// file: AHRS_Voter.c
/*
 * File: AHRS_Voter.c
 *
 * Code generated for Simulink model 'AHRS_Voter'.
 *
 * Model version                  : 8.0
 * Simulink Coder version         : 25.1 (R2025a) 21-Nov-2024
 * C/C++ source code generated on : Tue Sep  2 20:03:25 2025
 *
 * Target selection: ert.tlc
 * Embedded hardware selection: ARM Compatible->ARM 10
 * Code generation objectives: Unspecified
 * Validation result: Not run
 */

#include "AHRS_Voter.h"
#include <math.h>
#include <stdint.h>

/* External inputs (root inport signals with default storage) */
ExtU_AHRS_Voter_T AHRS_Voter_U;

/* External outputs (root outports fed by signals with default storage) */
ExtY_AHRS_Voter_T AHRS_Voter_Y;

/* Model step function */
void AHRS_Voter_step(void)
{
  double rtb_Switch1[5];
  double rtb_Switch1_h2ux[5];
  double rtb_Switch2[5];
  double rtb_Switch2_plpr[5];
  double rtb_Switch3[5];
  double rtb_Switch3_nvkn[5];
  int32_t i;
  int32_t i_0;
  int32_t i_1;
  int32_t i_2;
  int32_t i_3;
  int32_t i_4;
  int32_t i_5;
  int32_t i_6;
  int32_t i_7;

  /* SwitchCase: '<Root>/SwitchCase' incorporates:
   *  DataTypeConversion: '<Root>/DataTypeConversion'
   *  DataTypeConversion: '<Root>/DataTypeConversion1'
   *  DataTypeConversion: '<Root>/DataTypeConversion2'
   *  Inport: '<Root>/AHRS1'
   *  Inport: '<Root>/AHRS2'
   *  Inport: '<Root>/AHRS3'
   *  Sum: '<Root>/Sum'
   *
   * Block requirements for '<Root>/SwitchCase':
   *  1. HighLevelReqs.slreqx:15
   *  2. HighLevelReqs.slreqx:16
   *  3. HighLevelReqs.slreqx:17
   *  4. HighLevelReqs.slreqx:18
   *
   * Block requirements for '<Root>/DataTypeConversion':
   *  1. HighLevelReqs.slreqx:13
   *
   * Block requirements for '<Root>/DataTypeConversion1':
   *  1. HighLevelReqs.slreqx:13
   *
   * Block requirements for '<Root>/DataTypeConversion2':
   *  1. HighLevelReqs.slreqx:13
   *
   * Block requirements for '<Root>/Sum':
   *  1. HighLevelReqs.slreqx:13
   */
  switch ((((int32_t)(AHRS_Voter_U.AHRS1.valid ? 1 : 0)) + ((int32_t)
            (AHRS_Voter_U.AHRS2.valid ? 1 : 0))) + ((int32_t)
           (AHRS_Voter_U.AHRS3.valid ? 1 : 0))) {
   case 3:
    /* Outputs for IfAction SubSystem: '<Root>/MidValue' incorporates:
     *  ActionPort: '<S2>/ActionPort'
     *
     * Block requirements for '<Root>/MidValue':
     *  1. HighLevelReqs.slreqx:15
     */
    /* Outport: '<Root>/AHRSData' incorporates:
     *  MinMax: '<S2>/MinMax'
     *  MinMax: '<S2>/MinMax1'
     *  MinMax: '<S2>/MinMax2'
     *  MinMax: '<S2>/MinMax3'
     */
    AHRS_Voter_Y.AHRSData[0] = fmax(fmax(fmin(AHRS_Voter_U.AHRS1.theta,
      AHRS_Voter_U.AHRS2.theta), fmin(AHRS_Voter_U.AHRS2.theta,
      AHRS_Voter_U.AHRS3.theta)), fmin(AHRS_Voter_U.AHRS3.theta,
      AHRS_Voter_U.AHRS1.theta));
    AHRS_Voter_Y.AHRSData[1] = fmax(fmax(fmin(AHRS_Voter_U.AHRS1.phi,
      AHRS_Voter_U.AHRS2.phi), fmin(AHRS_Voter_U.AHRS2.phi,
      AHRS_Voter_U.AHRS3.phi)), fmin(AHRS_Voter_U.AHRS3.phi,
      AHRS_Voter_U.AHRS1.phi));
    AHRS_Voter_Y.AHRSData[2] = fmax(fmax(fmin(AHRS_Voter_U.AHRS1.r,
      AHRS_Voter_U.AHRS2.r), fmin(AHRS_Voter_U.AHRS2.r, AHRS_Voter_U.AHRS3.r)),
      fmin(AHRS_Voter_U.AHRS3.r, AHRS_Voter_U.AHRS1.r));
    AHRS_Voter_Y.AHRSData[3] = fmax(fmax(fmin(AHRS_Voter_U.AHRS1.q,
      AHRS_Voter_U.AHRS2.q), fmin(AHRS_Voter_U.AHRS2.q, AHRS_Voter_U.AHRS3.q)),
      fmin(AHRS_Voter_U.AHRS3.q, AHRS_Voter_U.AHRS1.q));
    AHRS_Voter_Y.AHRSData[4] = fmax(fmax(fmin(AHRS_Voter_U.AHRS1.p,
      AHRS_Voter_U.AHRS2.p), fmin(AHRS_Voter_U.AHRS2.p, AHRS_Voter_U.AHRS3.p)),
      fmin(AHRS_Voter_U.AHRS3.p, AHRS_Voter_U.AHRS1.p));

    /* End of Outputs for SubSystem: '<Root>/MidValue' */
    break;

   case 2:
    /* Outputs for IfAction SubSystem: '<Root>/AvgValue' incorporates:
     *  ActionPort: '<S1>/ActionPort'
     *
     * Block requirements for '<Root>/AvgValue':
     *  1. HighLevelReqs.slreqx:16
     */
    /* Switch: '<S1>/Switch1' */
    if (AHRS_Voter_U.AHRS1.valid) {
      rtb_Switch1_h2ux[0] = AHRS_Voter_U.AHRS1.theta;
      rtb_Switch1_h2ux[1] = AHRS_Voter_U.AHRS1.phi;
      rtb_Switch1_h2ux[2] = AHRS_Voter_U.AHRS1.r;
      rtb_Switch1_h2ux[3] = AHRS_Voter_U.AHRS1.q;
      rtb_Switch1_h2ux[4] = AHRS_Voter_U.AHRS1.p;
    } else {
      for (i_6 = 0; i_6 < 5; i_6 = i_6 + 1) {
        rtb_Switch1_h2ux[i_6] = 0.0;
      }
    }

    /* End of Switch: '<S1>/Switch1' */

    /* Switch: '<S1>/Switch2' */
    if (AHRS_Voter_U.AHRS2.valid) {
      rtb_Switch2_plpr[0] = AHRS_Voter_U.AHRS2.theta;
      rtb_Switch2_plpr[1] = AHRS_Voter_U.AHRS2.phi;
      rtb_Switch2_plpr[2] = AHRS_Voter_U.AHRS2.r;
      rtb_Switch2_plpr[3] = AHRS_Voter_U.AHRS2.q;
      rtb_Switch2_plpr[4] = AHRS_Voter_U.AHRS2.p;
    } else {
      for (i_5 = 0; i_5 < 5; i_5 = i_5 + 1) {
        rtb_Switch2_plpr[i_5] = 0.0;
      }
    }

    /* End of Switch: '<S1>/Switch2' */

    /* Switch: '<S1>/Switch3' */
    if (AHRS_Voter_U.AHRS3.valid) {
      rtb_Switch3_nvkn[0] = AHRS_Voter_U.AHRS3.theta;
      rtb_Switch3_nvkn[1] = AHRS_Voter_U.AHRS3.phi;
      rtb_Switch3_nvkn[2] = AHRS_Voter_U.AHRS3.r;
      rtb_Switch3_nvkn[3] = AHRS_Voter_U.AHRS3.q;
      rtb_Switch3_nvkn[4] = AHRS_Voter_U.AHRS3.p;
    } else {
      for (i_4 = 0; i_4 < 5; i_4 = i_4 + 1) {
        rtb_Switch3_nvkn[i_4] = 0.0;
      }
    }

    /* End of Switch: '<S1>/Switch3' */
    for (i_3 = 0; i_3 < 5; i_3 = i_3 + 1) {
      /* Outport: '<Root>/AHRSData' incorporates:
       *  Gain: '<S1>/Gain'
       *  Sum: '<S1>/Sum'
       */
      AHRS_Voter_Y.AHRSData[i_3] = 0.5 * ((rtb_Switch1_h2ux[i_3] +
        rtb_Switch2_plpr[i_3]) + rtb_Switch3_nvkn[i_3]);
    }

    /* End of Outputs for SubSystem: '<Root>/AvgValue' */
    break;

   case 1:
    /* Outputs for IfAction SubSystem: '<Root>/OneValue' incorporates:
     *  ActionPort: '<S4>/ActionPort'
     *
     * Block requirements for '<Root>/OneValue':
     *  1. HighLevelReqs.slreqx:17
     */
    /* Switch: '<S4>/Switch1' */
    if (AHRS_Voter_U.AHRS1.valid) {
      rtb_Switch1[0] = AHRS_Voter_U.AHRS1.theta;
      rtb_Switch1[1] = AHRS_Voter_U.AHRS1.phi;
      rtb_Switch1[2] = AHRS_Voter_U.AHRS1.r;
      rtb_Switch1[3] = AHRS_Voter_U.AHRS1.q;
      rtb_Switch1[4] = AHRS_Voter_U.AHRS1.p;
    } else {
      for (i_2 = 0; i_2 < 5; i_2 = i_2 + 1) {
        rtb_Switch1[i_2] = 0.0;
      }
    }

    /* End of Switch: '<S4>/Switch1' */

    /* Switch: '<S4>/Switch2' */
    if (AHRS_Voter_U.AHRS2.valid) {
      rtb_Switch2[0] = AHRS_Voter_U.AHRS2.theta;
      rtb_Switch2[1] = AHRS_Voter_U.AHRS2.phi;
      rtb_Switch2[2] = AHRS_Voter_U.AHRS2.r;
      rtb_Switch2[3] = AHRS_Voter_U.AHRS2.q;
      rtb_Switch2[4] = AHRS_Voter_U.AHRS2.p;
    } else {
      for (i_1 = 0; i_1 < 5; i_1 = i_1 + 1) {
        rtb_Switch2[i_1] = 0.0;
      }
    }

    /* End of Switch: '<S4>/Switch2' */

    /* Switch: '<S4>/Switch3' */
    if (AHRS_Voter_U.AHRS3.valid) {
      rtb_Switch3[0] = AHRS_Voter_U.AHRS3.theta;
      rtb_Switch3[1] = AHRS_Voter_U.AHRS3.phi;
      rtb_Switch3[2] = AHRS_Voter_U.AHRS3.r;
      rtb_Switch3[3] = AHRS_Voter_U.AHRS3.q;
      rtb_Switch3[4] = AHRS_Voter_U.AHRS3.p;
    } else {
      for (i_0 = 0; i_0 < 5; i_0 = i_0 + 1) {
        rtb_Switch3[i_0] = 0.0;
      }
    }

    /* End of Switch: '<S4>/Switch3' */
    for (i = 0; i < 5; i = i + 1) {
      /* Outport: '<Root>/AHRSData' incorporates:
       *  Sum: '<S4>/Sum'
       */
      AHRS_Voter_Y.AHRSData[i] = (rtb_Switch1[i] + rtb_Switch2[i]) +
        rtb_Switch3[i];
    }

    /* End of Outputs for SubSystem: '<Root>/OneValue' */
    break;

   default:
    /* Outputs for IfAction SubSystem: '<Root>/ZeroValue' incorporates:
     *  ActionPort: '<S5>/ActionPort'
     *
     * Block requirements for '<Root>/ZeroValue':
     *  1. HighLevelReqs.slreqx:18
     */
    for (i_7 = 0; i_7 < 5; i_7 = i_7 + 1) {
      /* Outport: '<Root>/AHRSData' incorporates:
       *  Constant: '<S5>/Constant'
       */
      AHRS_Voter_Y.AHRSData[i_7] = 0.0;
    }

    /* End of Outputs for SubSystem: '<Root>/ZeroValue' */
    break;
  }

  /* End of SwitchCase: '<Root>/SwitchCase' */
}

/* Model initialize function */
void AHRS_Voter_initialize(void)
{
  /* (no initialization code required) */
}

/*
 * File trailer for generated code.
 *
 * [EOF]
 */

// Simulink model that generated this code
simulink model "AHRS_Voter"  (R2024b)
settings: configuration reference "csSingleInstance" (kept outside this file)
libraries: simulink x1

== system AHRS_Voter ==
  AHRS1 : Inport  OutDataTypeStr=Bus: AHRS_Bus  PortDimensions=1  SampleTime=0.01  BusOutputAsStruct=on
  AHRS2 : Inport  Port=2  OutDataTypeStr=Bus: AHRS_Bus  PortDimensions=1  SampleTime=0.01  BusOutputAsStruct=on
  AHRS3 : Inport  Port=3  OutDataTypeStr=Bus: AHRS_Bus  PortDimensions=1  SampleTime=0.01  BusOutputAsStruct=on
  AvgValue : Subsystem  TreatAsAtomicUnit=on
  BusSelector : BusSelector  OutputSignals=valid
  BusSelector1 : BusSelector  OutputSignals=valid
  BusSelector2 : BusSelector  OutputSignals=valid
  BusSelector3 : BusSelector  OutputSignals=theta,phi,r,q,p
  BusSelector4 : BusSelector  OutputSignals=theta,phi,r,q,p
  BusSelector5 : BusSelector  OutputSignals=theta,phi,r,q,p
  DataTypeConversion : DataTypeConversion  OutDataTypeStr=int32  SaturateOnIntegerOverflow=off  RndMeth=Floor
  DataTypeConversion1 : DataTypeConversion  OutDataTypeStr=int32  SaturateOnIntegerOverflow=off  RndMeth=Floor
  DataTypeConversion2 : DataTypeConversion  OutDataTypeStr=int32  SaturateOnIntegerOverflow=off  RndMeth=Floor
  Merge : Merge  Inputs=4
  MidValue : Subsystem  TreatAsAtomicUnit=on
  Model Info : simulink/Model-Wide Utilities/Model Info  Frame=on  DisplayStringWithTags=|  HorizontalTextAlignment=Center  LeftAlignmentValue=0.5
      | Model Name: %<ModelName>
      | Model Version: %<ModelVersion>
      | Last Modified: %<LastModificationDate>
  Mux : Mux  Inputs=5
  Mux1 : Mux  Inputs=5
  Mux2 : Mux  Inputs=5
  OneValue : Subsystem  TreatAsAtomicUnit=on
  SignalConversion : SignalConversion  OverrideOpt=on
  Sum : Sum  Inputs=+++  OutDataTypeStr=int32
  SwitchCase : SwitchCase  CaseConditions={3, 2, 1}
  ZeroValue : Subsystem  TreatAsAtomicUnit=on
  AHRSData : Outport  OutDataTypeStr=double  VectorParamsAs1DForOutWhenUnconnected=off
  wires:
  Sum/1 -> SwitchCase/1
  AHRS1/1 -> BusSelector/1, BusSelector3/1
  AHRS2/1 -> BusSelector4/1, BusSelector1/1
  AHRS3/1 -> BusSelector5/1, BusSelector2/1
  BusSelector/1 -> DataTypeConversion/1, AvgValue/4(AHRS1_Valid), OneValue/4(AHRS1_Valid)  "<valid>"
  BusSelector1/1 -> DataTypeConversion1/1, AvgValue/5(AHRS2_Valid), OneValue/5(AHRS2_Valid)  "<valid>"
  BusSelector2/1 -> DataTypeConversion2/1, AvgValue/6(AHRS3_Valid), OneValue/6(AHRS3_Valid)  "<valid>"
  Mux/1 -> OneValue/1(AHRS1), AvgValue/1(AHRS1), MidValue/1(AHRS1)
  BusSelector3/1 -> Mux/1  "<theta>"
  BusSelector3/2 -> Mux/2  "<phi>"
  BusSelector3/3 -> Mux/3  "<r>"
  BusSelector3/4 -> Mux/4  "<q>"
  BusSelector3/5 -> Mux/5  "<p>"
  BusSelector4/1 -> Mux1/1  "<theta>"
  BusSelector4/2 -> Mux1/2  "<phi>"
  BusSelector4/3 -> Mux1/3  "<r>"
  BusSelector4/4 -> Mux1/4  "<q>"
  BusSelector4/5 -> Mux1/5  "<p>"
  BusSelector5/1 -> Mux2/1  "<theta>"
  BusSelector5/2 -> Mux2/2  "<phi>"
  BusSelector5/3 -> Mux2/3  "<r>"
  BusSelector5/4 -> Mux2/4  "<q>"
  BusSelector5/5 -> Mux2/5  "<p>"
  Mux1/1 -> AvgValue/2(AHRS2), OneValue/2(AHRS2), MidValue/2(AHRS2)
  Mux2/1 -> AvgValue/3(AHRS3), OneValue/3(AHRS3), MidValue/3(AHRS3)
  SwitchCase/4 -> ZeroValue/Action
  SwitchCase/3 -> OneValue/Action
  SwitchCase/2 -> AvgValue/Action
  SwitchCase/1 -> MidValue/Action
  Merge/1 -> SignalConversion/1
  ZeroValue/1(AvgValue) -> Merge/1
  OneValue/1(AvgValue) -> Merge/2
  AvgValue/1(AvgValue) -> Merge/3
  MidValue/1(MidValue) -> Merge/4
  DataTypeConversion/1 -> Sum/1
  DataTypeConversion1/1 -> Sum/2
  DataTypeConversion2/1 -> Sum/3
  SignalConversion/1 -> AHRSData/1

== system AHRS_Voter/AvgValue ==
  AHRS1 : Inport
  AHRS2 : Inport  Port=2
  AHRS3 : Inport  Port=3
  AHRS1_Valid : Inport  Port=4  OutDataTypeStr=boolean  PortDimensions=1
  AHRS2_Valid : Inport  Port=5  OutDataTypeStr=boolean  PortDimensions=1
  AHRS3_Valid : Inport  Port=6  OutDataTypeStr=boolean  PortDimensions=1
  ActionPort : ActionPort  ActionPortLabel=case [ 2 ]:
  Constant : Constant  Value=[0,0,0,0,0]
  Gain : Gain  Gain=1/2
  Sum : Sum  Inputs=+++
  Switch1 : Switch  Criteria=u2 ~= 0  SaturateOnIntegerOverflow=off  InputSameDT=off
  Switch2 : Switch  Criteria=u2 ~= 0  SaturateOnIntegerOverflow=off  InputSameDT=off
  Switch3 : Switch  Criteria=u2 ~= 0  SaturateOnIntegerOverflow=off  InputSameDT=off
  AvgValue : Outport  VectorParamsAs1DForOutWhenUnconnected=off
  wires:
  AHRS3/1 -> Switch3/1
  AHRS2/1 -> Switch2/1
  AHRS3_Valid/1 -> Switch3/2
  AHRS2_Valid/1 -> Switch2/2
  Switch3/1 -> Sum/3
  Switch2/1 -> Sum/2
  Switch1/1 -> Sum/1
  AHRS1/1 -> Switch1/1
  AHRS1_Valid/1 -> Switch1/2
  Sum/1 -> Gain/1
  Gain/1 -> AvgValue/1
  Constant/1 -> Switch3/3, Switch2/3, Switch1/3

== system AHRS_Voter/MidValue ==
  AHRS1 : Inport
  AHRS2 : Inport  Port=2
  AHRS3 : Inport  Port=3
  ActionPort : ActionPort  ActionPortLabel=case [ 3 ]:
  MinMax : MinMax  Function=max  Inputs=3
  MinMax1 : MinMax  Inputs=2
  MinMax2 : MinMax  Inputs=2
  MinMax3 : MinMax  Inputs=2
  MidValue : Outport  VectorParamsAs1DForOutWhenUnconnected=off
  wires:
  MinMax/1 -> MidValue/1
  MinMax2/1 -> MinMax/2
  AHRS2/1 -> MinMax2/1, MinMax1/2
  AHRS3/1 -> MinMax3/1, MinMax2/2
  AHRS1/1 -> MinMax1/1, MinMax3/2
  MinMax1/1 -> MinMax/1
  MinMax3/1 -> MinMax/3

== system AHRS_Voter/OneValue ==
  AHRS1 : Inport
  AHRS2 : Inport  Port=2
  AHRS3 : Inport  Port=3
  AHRS1_Valid : Inport  Port=4  OutDataTypeStr=boolean  PortDimensions=1
  AHRS2_Valid : Inport  Port=5  OutDataTypeStr=boolean  PortDimensions=1
  AHRS3_Valid : Inport  Port=6  OutDataTypeStr=boolean  PortDimensions=1
  ActionPort : ActionPort  ActionPortLabel=case [ 1 ]:
  Constant : Constant  Value=[0,0,0,0,0]
  Sum : Sum  Inputs=+++
  Switch1 : Switch  Criteria=u2 ~= 0  SaturateOnIntegerOverflow=off  InputSameDT=off
  Switch2 : Switch  Criteria=u2 ~= 0  SaturateOnIntegerOverflow=off  InputSameDT=off
  Switch3 : Switch  Criteria=u2 ~= 0  SaturateOnIntegerOverflow=off  InputSameDT=off
  AvgValue : Outport  VectorParamsAs1DForOutWhenUnconnected=off
  wires:
  Constant/1 -> Switch1/3, Switch2/3, Switch3/3
  Sum/1 -> AvgValue/1
  AHRS1_Valid/1 -> Switch1/2
  AHRS1/1 -> Switch1/1
  Switch1/1 -> Sum/1
  Switch2/1 -> Sum/2
  Switch3/1 -> Sum/3
  AHRS2_Valid/1 -> Switch2/2
  AHRS3_Valid/1 -> Switch3/2
  AHRS2/1 -> Switch2/1
  AHRS3/1 -> Switch3/1

== system AHRS_Voter/ZeroValue ==
  ActionPort : ActionPort  ActionPortLabel=default:
  Constant : Constant  Value=[0,0,0,0,0]  SampleTime=-1
  AvgValue : Outport  VectorParamsAs1DForOutWhenUnconnected=off
  wires:
  Constant/1 -> AvgValue/1
